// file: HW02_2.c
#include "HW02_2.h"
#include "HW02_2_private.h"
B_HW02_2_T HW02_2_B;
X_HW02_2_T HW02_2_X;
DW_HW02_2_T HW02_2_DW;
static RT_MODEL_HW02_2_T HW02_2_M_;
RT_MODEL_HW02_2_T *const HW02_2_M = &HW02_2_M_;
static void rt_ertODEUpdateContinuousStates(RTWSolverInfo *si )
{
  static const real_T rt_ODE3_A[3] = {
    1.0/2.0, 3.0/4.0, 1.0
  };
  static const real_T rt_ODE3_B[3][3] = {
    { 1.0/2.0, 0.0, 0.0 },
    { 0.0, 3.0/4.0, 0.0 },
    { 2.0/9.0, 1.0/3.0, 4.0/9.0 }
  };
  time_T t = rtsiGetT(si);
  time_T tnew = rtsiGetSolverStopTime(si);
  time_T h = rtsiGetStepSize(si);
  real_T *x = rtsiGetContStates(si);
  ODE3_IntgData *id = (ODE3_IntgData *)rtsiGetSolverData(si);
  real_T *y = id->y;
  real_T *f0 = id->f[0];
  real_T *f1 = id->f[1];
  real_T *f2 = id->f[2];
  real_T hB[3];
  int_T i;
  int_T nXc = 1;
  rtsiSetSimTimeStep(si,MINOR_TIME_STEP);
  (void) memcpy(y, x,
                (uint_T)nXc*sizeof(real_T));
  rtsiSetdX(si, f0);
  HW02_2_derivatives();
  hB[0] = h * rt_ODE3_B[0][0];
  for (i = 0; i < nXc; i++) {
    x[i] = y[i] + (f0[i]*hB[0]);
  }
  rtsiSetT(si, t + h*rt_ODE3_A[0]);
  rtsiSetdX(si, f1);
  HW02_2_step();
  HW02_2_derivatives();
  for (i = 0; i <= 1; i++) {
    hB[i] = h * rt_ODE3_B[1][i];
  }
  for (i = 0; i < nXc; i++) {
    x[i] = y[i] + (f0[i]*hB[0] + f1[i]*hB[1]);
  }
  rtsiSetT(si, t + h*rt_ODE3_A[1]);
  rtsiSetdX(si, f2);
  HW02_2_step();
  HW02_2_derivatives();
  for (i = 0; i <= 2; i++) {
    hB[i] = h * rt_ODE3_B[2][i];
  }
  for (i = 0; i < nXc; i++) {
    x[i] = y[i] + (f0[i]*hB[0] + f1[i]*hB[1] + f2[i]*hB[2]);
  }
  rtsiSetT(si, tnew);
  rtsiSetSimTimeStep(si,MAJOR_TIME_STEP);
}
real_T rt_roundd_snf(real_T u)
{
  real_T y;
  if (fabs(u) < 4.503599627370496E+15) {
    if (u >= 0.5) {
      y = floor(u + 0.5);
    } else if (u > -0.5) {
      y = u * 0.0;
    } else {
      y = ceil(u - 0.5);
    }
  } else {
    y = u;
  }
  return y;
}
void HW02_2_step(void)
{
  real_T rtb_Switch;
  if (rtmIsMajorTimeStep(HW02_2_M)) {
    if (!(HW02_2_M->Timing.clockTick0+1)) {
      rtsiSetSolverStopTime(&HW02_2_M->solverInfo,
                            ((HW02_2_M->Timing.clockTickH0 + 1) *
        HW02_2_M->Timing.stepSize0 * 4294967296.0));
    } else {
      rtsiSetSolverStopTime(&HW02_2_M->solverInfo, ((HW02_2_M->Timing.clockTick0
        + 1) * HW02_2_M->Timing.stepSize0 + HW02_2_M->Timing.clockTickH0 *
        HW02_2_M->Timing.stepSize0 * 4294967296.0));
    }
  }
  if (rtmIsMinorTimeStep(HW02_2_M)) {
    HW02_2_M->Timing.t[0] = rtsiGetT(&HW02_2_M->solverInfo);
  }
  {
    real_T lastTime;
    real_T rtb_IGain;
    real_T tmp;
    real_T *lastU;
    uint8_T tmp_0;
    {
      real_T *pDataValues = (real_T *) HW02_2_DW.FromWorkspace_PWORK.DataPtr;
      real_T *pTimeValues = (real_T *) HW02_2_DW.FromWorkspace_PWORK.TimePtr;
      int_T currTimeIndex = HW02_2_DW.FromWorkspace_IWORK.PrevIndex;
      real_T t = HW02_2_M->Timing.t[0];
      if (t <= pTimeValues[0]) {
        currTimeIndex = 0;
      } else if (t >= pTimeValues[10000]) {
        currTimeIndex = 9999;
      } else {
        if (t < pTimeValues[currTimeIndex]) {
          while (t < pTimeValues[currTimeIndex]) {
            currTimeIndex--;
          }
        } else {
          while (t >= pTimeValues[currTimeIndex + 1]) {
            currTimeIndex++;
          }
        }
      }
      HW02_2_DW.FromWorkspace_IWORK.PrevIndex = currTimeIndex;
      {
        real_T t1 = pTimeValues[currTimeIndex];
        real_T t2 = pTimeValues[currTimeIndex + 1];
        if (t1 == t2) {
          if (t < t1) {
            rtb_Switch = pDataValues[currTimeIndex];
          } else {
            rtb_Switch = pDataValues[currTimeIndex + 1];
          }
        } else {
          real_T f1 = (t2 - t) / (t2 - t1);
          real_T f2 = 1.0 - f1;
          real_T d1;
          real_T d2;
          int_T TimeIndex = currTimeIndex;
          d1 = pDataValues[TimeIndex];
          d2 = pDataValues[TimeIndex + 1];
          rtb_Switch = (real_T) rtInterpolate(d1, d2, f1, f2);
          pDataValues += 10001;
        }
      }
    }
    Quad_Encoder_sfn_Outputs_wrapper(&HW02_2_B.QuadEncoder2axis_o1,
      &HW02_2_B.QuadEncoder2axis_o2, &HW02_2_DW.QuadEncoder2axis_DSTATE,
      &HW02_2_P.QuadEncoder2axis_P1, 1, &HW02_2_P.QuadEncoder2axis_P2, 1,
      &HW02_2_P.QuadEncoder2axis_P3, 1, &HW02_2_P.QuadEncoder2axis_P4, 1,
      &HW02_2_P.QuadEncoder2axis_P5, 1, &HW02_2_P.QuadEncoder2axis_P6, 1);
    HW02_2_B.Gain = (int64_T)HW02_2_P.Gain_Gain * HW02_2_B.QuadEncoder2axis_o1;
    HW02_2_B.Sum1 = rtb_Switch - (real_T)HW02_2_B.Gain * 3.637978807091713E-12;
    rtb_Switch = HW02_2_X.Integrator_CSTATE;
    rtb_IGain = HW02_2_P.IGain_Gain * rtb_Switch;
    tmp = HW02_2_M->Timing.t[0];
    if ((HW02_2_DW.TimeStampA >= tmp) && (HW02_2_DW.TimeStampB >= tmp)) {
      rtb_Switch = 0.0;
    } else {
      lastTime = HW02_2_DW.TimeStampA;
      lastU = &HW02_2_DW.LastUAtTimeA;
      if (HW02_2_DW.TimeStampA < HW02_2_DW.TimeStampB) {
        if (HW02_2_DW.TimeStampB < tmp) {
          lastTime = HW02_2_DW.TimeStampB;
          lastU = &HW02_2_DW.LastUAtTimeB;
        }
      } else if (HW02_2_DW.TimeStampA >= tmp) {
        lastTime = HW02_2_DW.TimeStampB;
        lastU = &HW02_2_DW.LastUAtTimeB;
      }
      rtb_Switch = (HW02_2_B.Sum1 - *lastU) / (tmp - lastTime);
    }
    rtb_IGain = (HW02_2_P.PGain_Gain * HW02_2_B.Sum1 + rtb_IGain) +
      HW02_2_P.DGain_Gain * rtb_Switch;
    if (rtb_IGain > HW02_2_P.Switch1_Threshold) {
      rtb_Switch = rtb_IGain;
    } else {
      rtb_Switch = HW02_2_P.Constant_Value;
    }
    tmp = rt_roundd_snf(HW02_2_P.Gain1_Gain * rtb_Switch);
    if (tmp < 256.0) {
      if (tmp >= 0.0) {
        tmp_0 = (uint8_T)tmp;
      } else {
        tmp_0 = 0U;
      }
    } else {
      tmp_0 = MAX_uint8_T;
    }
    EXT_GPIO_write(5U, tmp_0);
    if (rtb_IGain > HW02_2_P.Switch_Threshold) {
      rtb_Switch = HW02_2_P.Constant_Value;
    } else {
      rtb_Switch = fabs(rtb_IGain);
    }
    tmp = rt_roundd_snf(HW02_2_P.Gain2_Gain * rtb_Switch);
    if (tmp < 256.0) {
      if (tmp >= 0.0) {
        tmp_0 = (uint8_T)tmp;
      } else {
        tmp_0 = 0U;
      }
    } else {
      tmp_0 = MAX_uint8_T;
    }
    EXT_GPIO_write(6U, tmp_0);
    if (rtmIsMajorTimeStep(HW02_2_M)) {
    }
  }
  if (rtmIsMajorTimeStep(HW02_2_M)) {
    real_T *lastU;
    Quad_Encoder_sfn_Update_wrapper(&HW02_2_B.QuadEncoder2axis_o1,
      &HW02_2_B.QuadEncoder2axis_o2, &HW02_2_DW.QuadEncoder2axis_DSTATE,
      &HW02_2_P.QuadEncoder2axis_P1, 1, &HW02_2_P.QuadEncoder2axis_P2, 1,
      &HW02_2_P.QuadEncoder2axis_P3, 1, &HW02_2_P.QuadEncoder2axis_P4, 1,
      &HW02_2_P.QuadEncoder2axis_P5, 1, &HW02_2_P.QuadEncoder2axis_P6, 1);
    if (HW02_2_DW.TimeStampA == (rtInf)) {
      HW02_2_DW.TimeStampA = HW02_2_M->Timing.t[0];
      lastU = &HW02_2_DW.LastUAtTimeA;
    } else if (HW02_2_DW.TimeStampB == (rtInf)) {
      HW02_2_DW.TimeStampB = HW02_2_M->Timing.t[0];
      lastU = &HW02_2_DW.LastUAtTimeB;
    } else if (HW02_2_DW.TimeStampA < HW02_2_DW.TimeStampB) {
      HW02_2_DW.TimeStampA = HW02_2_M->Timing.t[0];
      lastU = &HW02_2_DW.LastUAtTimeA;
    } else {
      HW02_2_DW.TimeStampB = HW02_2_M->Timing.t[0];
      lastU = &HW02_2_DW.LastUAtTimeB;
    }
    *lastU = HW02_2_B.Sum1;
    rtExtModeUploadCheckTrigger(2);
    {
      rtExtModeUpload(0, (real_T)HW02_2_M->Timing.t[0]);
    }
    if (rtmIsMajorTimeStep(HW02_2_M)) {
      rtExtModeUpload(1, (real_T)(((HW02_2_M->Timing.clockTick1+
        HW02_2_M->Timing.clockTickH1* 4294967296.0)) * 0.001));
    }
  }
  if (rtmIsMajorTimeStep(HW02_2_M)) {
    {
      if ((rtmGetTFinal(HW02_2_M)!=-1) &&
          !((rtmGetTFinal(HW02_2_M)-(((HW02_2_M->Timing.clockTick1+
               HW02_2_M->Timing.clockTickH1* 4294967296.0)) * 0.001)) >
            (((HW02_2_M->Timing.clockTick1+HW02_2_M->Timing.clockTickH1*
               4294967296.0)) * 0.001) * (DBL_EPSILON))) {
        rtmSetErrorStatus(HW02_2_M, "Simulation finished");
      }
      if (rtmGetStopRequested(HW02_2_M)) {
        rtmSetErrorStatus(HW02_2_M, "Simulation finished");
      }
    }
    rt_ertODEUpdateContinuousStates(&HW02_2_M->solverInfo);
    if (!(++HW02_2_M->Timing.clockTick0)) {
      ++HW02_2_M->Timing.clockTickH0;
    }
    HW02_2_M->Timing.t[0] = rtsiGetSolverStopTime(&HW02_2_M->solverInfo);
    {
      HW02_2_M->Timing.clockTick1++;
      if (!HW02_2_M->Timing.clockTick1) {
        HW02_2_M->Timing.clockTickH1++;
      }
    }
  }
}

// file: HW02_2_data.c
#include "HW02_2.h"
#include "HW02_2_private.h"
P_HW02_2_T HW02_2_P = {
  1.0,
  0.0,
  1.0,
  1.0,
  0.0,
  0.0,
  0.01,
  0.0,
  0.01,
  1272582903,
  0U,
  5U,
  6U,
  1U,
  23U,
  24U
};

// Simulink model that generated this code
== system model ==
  GPIOWrite#1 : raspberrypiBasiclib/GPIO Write  <- 1: Gain1
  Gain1 : Gain  Gain=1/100  <- 1: Switch1
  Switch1 : Switch  Criteria=u2 > Threshold  <- 1: Sum#1, 2: Sum#1, 3: Constant
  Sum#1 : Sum  Inputs=+++  <- 1: PGain, 2: IGain, 3: DGain
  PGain : Gain  <- 1: Sum1
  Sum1 : Sum  Inputs=+-  <- 1: FromWorkspace, 2: Gain
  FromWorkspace : FromWorkspace
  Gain : Gain  Gain=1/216  <- 1: QuadEncoder2axis
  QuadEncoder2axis : S-Function  FunctionName=Quad_Encoder_sfn
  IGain : Gain  <- 1: Integrator
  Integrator : Integrator  <- 1: Sum1
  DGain : Gain  <- 1: Derivative#1
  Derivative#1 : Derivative  <- 1: Sum1
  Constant : Constant  Value=0
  GPIOWrite#2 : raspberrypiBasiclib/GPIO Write  <- 1: Gain2
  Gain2 : Gain  Gain=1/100  <- 1: Switch
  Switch : Switch  Criteria=u2 > Threshold  <- 1: Constant, 2: Sum#1, 3: Abs#1
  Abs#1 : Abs  <- 1: Sum#1
